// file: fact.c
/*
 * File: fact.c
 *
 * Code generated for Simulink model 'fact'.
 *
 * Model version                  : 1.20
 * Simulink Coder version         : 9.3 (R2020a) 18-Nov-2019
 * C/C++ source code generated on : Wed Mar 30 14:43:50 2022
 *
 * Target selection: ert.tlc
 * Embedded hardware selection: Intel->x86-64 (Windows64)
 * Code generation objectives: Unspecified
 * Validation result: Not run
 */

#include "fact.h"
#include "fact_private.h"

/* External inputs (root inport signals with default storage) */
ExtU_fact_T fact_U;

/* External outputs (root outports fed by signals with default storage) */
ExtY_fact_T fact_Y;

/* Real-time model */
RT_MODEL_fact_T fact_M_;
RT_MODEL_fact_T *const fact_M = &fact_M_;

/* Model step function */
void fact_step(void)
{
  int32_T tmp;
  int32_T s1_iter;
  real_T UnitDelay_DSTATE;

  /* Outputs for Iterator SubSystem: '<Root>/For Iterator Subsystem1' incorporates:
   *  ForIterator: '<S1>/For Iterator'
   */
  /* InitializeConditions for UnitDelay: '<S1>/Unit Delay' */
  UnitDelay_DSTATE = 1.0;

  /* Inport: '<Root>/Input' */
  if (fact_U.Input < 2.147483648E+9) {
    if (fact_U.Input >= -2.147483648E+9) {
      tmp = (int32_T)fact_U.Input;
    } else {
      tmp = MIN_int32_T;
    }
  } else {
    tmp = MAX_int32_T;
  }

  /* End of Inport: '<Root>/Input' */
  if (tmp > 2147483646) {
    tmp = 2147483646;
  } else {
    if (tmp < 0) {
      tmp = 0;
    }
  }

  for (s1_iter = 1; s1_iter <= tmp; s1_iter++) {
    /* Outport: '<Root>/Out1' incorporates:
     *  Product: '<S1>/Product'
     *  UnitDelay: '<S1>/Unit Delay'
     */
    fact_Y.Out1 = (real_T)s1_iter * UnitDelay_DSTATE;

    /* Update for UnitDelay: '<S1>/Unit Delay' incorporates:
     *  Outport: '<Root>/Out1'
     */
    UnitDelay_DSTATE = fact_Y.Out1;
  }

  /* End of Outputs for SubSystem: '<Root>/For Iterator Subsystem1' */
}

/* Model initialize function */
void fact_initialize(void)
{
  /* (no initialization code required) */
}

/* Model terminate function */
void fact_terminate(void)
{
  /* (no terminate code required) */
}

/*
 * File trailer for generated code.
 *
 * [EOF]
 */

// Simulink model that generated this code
simulink model "fact"  (R2020a)
settings: Solver=FixedStepDiscrete  StartTime=0.0  StopTime=10.0  RelTol=1e-3

== system fact ==
  Input : Inport
  For Iterator Subsystem1 : Subsystem  TreatAsAtomicUnit=on
  Out1 : Outport
  wires:
  For Iterator Subsystem1/1(Out1) -> Out1/1
  Input/1 -> For Iterator Subsystem1/1(Input)

== system fact/For Iterator Subsystem1 ==
  Input : Inport
  For Iterator : ForIterator  ResetStates=reset  IterationSource=external  IterationVariableDataType=double
  Product : Product
  Unit Delay : UnitDelay  InitialCondition=1  SampleTime=-1  HasFrameUpgradeWarning=on
  Out1 : Outport
  wires:
  Input/1 -> For Iterator/1
  For Iterator/1 -> Product/1
  Product/1 -> Unit Delay/1, Out1/1
  Unit Delay/1 -> Product/2
